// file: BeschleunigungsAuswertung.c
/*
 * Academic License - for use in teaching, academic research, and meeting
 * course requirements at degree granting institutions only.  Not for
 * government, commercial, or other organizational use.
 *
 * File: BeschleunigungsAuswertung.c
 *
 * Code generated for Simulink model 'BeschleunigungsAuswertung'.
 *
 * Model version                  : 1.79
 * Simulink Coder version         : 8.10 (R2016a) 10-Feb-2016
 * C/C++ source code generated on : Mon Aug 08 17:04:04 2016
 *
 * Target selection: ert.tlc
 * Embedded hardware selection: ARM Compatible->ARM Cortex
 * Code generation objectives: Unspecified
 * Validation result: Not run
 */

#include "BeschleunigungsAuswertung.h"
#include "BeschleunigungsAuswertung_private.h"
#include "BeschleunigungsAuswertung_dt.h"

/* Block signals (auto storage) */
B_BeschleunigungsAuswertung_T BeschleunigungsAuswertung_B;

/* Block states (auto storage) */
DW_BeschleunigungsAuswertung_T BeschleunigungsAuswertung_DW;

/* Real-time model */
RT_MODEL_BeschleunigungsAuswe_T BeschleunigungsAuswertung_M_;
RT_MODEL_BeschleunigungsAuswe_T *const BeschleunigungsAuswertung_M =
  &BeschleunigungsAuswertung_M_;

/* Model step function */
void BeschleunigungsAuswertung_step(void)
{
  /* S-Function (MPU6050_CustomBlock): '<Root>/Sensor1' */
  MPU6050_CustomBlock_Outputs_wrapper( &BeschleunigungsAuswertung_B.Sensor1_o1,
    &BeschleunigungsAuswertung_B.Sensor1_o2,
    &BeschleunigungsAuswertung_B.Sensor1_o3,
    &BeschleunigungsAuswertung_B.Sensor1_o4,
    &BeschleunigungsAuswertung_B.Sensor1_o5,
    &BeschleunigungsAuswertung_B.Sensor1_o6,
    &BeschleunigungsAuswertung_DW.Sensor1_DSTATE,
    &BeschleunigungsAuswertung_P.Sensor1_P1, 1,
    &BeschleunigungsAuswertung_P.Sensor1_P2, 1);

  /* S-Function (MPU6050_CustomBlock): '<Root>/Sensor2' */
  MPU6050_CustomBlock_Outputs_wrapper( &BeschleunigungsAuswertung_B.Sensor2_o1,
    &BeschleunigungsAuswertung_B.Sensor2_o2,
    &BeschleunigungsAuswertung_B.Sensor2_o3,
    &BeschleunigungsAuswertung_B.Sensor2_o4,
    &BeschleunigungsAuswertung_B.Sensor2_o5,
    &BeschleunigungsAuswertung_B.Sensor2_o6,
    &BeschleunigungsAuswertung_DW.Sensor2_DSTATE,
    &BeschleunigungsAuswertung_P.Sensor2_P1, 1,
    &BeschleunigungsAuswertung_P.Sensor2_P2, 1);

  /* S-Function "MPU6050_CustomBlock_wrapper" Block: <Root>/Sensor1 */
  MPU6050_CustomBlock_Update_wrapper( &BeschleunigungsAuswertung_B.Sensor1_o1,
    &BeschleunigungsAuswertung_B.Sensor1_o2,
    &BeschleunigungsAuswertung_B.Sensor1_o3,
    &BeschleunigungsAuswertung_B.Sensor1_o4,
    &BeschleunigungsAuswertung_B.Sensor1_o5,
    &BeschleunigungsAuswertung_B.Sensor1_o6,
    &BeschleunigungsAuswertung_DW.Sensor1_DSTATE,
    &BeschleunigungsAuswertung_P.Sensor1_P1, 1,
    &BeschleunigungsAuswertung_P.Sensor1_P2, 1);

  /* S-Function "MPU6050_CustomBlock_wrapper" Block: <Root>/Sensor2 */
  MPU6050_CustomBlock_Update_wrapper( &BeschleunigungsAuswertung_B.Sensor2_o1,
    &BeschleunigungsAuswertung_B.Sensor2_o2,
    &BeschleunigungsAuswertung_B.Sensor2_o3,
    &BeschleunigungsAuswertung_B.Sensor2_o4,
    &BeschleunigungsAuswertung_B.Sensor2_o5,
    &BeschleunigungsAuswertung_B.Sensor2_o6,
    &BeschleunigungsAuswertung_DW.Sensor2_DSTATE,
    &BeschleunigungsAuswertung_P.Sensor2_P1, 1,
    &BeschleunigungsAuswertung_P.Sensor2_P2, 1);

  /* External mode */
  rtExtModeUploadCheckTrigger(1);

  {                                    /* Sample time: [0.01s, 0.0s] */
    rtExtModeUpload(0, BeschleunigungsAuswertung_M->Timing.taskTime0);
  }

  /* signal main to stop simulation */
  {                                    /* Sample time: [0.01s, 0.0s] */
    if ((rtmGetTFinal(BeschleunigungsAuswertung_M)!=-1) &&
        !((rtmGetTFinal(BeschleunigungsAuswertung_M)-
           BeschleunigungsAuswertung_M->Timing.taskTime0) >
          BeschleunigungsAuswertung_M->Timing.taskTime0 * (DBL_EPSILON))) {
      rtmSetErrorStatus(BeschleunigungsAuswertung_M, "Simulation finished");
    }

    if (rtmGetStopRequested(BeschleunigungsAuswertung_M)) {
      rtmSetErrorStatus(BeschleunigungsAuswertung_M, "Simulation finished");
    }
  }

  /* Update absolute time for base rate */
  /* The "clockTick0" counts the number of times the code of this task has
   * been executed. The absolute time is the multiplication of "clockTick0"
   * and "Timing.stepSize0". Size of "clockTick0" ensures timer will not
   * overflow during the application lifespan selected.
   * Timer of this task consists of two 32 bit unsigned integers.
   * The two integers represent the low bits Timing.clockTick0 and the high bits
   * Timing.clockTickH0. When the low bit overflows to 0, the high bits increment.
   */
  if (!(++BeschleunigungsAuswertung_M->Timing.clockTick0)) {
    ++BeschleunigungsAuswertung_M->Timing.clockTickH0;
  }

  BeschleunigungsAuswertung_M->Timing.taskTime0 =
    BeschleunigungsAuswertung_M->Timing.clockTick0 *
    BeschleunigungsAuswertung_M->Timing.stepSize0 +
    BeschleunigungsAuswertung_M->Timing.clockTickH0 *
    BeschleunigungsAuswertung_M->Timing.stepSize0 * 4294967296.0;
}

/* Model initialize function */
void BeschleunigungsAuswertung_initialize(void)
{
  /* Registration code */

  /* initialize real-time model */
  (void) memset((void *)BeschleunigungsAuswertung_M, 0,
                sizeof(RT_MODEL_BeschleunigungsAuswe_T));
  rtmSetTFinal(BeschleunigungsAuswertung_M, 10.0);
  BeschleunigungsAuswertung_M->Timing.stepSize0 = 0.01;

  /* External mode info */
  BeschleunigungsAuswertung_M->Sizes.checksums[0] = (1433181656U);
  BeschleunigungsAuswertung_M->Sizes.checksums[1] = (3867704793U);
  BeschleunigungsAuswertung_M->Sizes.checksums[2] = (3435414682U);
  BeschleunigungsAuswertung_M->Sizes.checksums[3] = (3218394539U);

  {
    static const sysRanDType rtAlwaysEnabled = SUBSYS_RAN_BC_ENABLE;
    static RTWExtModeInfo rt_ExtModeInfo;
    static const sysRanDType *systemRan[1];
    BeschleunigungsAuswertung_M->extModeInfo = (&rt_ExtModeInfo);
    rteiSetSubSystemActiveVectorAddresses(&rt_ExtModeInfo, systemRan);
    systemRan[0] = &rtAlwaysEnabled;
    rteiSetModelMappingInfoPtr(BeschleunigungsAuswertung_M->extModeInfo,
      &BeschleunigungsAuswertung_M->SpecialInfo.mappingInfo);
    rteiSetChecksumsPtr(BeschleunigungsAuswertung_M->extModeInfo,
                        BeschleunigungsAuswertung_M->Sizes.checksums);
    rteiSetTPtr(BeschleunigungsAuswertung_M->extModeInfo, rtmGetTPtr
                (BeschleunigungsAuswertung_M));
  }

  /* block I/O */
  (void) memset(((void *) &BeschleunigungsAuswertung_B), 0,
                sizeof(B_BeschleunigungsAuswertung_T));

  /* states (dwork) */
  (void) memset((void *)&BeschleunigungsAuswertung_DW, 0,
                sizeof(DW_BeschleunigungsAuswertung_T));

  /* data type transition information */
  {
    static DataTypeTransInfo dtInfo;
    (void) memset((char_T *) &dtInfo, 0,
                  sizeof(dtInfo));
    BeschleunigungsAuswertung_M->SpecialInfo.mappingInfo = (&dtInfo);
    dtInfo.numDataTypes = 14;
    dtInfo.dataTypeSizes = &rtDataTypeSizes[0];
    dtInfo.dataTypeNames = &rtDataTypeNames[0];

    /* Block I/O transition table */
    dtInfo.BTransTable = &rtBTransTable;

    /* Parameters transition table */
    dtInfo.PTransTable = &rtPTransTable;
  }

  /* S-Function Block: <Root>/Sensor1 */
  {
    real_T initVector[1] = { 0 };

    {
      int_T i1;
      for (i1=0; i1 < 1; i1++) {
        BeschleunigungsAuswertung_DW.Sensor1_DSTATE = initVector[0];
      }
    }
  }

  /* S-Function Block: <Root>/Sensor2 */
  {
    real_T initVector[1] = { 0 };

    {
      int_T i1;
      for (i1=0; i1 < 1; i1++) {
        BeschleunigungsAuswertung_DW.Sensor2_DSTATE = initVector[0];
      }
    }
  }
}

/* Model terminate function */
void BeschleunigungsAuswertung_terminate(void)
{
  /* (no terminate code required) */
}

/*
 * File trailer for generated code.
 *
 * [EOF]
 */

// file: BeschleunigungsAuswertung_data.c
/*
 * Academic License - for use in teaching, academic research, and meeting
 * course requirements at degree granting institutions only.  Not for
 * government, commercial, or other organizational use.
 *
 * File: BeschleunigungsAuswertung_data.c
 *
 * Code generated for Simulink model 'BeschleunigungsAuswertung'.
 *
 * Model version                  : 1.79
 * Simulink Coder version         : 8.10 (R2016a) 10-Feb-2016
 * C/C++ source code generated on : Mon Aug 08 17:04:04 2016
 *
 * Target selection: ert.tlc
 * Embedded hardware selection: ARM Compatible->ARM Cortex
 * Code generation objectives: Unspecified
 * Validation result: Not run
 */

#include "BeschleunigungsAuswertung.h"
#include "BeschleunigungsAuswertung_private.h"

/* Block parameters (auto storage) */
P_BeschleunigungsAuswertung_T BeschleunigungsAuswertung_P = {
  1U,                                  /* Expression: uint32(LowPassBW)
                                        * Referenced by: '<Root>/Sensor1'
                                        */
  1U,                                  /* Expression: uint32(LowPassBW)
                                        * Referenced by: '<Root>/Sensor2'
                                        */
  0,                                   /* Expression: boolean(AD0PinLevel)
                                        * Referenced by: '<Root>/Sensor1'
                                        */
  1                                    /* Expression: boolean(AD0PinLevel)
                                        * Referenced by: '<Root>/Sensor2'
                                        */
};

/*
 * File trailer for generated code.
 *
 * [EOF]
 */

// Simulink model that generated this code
simulink model "BeschleunigungsAuswertung"  (R2016a)
settings: Solver=FixedStepAuto  StartTime=0.0  StopTime=10  FixedStep=0.01  RelTol=1e-3
StopFcn:
  | AuswertungSensorenBeschleunigung

== system BeschleunigungsAuswertung ==
  Sensor1 : S-Function  InitFcn=try, set_param(gcb,'FunctionName','MPU6050_CustomBlock'), end  FunctionName=MPU6050_CustomBlock  Parameters=boolean(AD0PinLevel),uint32(LowPassBW)  SFunctionModules=MPU6050_CustomBlock_wrapper  SFunctionDeploymentMode=off  EnableBusSupport=off  mask(S-Function Builder){AD0PinLevel=0, LowPassBW=260}
      mask prompts: AD0PinLevel "Logic-Level of AD0 Pin"; LowPassBW "Low-Pass-Bandwidth [Hz]"
      mask help: Simulink:masks:SFunctionBuilder_MD
      mask init:
      | val = [[.9  0.75 0.75 1 1 .9 .9 1]',[1 1 0.75 0.75 .9 .9 1 .9]'];try , sys = get_param(gcb,'SfunBuilderFcnName');if isempty(sys), sys = get_param(gcb,'FunctionName'); end,catch, sys = get_param(gcb,'FunctionName'); end
  Sensor2 : S-Function  InitFcn=try, set_param(gcb,'FunctionName','MPU6050_CustomBlock'), end  FunctionName=MPU6050_CustomBlock  Parameters=boolean(AD0PinLevel),uint32(LowPassBW)  SFunctionModules=MPU6050_CustomBlock_wrapper  SFunctionDeploymentMode=off  EnableBusSupport=off  mask(S-Function Builder){AD0PinLevel=1, LowPassBW=260}
      mask prompts: AD0PinLevel "Logic-Level of AD0 Pin"; LowPassBW "Low-Pass-Bandwidth [Hz]"
      mask help: Simulink:masks:SFunctionBuilder_MD
      mask init: same as BeschleunigungsAuswertung/Sensor1
  Terminator{,1..7} (8 alike) : Terminator
  To Workspace : ToWorkspace  VariableName=x1__dd  SaveFormat=Structure With Time  SampleTime=-1
  To Workspace1 : ToWorkspace  VariableName=y1__dd  SaveFormat=Structure With Time  SampleTime=-1
  To Workspace2 : ToWorkspace  VariableName=y2__dd  SaveFormat=Structure With Time  SampleTime=-1
  To Workspace3 : ToWorkspace  VariableName=x2__dd  SaveFormat=Structure With Time  SampleTime=-1
  wires:
  Sensor2/1 -> To Workspace3/1
  Sensor2/2 -> To Workspace2/1
  Sensor2/4 -> Terminator5/1
  Sensor2/5 -> Terminator6/1
  Sensor2/6 -> Terminator7/1
  Sensor1/1 -> To Workspace/1
  Sensor1/2 -> To Workspace1/1
  Sensor1/3 -> Terminator/1
  Sensor1/4 -> Terminator1/1
  Sensor1/5 -> Terminator2/1
  Sensor1/6 -> Terminator3/1
  Sensor2/3 -> Terminator4/1
